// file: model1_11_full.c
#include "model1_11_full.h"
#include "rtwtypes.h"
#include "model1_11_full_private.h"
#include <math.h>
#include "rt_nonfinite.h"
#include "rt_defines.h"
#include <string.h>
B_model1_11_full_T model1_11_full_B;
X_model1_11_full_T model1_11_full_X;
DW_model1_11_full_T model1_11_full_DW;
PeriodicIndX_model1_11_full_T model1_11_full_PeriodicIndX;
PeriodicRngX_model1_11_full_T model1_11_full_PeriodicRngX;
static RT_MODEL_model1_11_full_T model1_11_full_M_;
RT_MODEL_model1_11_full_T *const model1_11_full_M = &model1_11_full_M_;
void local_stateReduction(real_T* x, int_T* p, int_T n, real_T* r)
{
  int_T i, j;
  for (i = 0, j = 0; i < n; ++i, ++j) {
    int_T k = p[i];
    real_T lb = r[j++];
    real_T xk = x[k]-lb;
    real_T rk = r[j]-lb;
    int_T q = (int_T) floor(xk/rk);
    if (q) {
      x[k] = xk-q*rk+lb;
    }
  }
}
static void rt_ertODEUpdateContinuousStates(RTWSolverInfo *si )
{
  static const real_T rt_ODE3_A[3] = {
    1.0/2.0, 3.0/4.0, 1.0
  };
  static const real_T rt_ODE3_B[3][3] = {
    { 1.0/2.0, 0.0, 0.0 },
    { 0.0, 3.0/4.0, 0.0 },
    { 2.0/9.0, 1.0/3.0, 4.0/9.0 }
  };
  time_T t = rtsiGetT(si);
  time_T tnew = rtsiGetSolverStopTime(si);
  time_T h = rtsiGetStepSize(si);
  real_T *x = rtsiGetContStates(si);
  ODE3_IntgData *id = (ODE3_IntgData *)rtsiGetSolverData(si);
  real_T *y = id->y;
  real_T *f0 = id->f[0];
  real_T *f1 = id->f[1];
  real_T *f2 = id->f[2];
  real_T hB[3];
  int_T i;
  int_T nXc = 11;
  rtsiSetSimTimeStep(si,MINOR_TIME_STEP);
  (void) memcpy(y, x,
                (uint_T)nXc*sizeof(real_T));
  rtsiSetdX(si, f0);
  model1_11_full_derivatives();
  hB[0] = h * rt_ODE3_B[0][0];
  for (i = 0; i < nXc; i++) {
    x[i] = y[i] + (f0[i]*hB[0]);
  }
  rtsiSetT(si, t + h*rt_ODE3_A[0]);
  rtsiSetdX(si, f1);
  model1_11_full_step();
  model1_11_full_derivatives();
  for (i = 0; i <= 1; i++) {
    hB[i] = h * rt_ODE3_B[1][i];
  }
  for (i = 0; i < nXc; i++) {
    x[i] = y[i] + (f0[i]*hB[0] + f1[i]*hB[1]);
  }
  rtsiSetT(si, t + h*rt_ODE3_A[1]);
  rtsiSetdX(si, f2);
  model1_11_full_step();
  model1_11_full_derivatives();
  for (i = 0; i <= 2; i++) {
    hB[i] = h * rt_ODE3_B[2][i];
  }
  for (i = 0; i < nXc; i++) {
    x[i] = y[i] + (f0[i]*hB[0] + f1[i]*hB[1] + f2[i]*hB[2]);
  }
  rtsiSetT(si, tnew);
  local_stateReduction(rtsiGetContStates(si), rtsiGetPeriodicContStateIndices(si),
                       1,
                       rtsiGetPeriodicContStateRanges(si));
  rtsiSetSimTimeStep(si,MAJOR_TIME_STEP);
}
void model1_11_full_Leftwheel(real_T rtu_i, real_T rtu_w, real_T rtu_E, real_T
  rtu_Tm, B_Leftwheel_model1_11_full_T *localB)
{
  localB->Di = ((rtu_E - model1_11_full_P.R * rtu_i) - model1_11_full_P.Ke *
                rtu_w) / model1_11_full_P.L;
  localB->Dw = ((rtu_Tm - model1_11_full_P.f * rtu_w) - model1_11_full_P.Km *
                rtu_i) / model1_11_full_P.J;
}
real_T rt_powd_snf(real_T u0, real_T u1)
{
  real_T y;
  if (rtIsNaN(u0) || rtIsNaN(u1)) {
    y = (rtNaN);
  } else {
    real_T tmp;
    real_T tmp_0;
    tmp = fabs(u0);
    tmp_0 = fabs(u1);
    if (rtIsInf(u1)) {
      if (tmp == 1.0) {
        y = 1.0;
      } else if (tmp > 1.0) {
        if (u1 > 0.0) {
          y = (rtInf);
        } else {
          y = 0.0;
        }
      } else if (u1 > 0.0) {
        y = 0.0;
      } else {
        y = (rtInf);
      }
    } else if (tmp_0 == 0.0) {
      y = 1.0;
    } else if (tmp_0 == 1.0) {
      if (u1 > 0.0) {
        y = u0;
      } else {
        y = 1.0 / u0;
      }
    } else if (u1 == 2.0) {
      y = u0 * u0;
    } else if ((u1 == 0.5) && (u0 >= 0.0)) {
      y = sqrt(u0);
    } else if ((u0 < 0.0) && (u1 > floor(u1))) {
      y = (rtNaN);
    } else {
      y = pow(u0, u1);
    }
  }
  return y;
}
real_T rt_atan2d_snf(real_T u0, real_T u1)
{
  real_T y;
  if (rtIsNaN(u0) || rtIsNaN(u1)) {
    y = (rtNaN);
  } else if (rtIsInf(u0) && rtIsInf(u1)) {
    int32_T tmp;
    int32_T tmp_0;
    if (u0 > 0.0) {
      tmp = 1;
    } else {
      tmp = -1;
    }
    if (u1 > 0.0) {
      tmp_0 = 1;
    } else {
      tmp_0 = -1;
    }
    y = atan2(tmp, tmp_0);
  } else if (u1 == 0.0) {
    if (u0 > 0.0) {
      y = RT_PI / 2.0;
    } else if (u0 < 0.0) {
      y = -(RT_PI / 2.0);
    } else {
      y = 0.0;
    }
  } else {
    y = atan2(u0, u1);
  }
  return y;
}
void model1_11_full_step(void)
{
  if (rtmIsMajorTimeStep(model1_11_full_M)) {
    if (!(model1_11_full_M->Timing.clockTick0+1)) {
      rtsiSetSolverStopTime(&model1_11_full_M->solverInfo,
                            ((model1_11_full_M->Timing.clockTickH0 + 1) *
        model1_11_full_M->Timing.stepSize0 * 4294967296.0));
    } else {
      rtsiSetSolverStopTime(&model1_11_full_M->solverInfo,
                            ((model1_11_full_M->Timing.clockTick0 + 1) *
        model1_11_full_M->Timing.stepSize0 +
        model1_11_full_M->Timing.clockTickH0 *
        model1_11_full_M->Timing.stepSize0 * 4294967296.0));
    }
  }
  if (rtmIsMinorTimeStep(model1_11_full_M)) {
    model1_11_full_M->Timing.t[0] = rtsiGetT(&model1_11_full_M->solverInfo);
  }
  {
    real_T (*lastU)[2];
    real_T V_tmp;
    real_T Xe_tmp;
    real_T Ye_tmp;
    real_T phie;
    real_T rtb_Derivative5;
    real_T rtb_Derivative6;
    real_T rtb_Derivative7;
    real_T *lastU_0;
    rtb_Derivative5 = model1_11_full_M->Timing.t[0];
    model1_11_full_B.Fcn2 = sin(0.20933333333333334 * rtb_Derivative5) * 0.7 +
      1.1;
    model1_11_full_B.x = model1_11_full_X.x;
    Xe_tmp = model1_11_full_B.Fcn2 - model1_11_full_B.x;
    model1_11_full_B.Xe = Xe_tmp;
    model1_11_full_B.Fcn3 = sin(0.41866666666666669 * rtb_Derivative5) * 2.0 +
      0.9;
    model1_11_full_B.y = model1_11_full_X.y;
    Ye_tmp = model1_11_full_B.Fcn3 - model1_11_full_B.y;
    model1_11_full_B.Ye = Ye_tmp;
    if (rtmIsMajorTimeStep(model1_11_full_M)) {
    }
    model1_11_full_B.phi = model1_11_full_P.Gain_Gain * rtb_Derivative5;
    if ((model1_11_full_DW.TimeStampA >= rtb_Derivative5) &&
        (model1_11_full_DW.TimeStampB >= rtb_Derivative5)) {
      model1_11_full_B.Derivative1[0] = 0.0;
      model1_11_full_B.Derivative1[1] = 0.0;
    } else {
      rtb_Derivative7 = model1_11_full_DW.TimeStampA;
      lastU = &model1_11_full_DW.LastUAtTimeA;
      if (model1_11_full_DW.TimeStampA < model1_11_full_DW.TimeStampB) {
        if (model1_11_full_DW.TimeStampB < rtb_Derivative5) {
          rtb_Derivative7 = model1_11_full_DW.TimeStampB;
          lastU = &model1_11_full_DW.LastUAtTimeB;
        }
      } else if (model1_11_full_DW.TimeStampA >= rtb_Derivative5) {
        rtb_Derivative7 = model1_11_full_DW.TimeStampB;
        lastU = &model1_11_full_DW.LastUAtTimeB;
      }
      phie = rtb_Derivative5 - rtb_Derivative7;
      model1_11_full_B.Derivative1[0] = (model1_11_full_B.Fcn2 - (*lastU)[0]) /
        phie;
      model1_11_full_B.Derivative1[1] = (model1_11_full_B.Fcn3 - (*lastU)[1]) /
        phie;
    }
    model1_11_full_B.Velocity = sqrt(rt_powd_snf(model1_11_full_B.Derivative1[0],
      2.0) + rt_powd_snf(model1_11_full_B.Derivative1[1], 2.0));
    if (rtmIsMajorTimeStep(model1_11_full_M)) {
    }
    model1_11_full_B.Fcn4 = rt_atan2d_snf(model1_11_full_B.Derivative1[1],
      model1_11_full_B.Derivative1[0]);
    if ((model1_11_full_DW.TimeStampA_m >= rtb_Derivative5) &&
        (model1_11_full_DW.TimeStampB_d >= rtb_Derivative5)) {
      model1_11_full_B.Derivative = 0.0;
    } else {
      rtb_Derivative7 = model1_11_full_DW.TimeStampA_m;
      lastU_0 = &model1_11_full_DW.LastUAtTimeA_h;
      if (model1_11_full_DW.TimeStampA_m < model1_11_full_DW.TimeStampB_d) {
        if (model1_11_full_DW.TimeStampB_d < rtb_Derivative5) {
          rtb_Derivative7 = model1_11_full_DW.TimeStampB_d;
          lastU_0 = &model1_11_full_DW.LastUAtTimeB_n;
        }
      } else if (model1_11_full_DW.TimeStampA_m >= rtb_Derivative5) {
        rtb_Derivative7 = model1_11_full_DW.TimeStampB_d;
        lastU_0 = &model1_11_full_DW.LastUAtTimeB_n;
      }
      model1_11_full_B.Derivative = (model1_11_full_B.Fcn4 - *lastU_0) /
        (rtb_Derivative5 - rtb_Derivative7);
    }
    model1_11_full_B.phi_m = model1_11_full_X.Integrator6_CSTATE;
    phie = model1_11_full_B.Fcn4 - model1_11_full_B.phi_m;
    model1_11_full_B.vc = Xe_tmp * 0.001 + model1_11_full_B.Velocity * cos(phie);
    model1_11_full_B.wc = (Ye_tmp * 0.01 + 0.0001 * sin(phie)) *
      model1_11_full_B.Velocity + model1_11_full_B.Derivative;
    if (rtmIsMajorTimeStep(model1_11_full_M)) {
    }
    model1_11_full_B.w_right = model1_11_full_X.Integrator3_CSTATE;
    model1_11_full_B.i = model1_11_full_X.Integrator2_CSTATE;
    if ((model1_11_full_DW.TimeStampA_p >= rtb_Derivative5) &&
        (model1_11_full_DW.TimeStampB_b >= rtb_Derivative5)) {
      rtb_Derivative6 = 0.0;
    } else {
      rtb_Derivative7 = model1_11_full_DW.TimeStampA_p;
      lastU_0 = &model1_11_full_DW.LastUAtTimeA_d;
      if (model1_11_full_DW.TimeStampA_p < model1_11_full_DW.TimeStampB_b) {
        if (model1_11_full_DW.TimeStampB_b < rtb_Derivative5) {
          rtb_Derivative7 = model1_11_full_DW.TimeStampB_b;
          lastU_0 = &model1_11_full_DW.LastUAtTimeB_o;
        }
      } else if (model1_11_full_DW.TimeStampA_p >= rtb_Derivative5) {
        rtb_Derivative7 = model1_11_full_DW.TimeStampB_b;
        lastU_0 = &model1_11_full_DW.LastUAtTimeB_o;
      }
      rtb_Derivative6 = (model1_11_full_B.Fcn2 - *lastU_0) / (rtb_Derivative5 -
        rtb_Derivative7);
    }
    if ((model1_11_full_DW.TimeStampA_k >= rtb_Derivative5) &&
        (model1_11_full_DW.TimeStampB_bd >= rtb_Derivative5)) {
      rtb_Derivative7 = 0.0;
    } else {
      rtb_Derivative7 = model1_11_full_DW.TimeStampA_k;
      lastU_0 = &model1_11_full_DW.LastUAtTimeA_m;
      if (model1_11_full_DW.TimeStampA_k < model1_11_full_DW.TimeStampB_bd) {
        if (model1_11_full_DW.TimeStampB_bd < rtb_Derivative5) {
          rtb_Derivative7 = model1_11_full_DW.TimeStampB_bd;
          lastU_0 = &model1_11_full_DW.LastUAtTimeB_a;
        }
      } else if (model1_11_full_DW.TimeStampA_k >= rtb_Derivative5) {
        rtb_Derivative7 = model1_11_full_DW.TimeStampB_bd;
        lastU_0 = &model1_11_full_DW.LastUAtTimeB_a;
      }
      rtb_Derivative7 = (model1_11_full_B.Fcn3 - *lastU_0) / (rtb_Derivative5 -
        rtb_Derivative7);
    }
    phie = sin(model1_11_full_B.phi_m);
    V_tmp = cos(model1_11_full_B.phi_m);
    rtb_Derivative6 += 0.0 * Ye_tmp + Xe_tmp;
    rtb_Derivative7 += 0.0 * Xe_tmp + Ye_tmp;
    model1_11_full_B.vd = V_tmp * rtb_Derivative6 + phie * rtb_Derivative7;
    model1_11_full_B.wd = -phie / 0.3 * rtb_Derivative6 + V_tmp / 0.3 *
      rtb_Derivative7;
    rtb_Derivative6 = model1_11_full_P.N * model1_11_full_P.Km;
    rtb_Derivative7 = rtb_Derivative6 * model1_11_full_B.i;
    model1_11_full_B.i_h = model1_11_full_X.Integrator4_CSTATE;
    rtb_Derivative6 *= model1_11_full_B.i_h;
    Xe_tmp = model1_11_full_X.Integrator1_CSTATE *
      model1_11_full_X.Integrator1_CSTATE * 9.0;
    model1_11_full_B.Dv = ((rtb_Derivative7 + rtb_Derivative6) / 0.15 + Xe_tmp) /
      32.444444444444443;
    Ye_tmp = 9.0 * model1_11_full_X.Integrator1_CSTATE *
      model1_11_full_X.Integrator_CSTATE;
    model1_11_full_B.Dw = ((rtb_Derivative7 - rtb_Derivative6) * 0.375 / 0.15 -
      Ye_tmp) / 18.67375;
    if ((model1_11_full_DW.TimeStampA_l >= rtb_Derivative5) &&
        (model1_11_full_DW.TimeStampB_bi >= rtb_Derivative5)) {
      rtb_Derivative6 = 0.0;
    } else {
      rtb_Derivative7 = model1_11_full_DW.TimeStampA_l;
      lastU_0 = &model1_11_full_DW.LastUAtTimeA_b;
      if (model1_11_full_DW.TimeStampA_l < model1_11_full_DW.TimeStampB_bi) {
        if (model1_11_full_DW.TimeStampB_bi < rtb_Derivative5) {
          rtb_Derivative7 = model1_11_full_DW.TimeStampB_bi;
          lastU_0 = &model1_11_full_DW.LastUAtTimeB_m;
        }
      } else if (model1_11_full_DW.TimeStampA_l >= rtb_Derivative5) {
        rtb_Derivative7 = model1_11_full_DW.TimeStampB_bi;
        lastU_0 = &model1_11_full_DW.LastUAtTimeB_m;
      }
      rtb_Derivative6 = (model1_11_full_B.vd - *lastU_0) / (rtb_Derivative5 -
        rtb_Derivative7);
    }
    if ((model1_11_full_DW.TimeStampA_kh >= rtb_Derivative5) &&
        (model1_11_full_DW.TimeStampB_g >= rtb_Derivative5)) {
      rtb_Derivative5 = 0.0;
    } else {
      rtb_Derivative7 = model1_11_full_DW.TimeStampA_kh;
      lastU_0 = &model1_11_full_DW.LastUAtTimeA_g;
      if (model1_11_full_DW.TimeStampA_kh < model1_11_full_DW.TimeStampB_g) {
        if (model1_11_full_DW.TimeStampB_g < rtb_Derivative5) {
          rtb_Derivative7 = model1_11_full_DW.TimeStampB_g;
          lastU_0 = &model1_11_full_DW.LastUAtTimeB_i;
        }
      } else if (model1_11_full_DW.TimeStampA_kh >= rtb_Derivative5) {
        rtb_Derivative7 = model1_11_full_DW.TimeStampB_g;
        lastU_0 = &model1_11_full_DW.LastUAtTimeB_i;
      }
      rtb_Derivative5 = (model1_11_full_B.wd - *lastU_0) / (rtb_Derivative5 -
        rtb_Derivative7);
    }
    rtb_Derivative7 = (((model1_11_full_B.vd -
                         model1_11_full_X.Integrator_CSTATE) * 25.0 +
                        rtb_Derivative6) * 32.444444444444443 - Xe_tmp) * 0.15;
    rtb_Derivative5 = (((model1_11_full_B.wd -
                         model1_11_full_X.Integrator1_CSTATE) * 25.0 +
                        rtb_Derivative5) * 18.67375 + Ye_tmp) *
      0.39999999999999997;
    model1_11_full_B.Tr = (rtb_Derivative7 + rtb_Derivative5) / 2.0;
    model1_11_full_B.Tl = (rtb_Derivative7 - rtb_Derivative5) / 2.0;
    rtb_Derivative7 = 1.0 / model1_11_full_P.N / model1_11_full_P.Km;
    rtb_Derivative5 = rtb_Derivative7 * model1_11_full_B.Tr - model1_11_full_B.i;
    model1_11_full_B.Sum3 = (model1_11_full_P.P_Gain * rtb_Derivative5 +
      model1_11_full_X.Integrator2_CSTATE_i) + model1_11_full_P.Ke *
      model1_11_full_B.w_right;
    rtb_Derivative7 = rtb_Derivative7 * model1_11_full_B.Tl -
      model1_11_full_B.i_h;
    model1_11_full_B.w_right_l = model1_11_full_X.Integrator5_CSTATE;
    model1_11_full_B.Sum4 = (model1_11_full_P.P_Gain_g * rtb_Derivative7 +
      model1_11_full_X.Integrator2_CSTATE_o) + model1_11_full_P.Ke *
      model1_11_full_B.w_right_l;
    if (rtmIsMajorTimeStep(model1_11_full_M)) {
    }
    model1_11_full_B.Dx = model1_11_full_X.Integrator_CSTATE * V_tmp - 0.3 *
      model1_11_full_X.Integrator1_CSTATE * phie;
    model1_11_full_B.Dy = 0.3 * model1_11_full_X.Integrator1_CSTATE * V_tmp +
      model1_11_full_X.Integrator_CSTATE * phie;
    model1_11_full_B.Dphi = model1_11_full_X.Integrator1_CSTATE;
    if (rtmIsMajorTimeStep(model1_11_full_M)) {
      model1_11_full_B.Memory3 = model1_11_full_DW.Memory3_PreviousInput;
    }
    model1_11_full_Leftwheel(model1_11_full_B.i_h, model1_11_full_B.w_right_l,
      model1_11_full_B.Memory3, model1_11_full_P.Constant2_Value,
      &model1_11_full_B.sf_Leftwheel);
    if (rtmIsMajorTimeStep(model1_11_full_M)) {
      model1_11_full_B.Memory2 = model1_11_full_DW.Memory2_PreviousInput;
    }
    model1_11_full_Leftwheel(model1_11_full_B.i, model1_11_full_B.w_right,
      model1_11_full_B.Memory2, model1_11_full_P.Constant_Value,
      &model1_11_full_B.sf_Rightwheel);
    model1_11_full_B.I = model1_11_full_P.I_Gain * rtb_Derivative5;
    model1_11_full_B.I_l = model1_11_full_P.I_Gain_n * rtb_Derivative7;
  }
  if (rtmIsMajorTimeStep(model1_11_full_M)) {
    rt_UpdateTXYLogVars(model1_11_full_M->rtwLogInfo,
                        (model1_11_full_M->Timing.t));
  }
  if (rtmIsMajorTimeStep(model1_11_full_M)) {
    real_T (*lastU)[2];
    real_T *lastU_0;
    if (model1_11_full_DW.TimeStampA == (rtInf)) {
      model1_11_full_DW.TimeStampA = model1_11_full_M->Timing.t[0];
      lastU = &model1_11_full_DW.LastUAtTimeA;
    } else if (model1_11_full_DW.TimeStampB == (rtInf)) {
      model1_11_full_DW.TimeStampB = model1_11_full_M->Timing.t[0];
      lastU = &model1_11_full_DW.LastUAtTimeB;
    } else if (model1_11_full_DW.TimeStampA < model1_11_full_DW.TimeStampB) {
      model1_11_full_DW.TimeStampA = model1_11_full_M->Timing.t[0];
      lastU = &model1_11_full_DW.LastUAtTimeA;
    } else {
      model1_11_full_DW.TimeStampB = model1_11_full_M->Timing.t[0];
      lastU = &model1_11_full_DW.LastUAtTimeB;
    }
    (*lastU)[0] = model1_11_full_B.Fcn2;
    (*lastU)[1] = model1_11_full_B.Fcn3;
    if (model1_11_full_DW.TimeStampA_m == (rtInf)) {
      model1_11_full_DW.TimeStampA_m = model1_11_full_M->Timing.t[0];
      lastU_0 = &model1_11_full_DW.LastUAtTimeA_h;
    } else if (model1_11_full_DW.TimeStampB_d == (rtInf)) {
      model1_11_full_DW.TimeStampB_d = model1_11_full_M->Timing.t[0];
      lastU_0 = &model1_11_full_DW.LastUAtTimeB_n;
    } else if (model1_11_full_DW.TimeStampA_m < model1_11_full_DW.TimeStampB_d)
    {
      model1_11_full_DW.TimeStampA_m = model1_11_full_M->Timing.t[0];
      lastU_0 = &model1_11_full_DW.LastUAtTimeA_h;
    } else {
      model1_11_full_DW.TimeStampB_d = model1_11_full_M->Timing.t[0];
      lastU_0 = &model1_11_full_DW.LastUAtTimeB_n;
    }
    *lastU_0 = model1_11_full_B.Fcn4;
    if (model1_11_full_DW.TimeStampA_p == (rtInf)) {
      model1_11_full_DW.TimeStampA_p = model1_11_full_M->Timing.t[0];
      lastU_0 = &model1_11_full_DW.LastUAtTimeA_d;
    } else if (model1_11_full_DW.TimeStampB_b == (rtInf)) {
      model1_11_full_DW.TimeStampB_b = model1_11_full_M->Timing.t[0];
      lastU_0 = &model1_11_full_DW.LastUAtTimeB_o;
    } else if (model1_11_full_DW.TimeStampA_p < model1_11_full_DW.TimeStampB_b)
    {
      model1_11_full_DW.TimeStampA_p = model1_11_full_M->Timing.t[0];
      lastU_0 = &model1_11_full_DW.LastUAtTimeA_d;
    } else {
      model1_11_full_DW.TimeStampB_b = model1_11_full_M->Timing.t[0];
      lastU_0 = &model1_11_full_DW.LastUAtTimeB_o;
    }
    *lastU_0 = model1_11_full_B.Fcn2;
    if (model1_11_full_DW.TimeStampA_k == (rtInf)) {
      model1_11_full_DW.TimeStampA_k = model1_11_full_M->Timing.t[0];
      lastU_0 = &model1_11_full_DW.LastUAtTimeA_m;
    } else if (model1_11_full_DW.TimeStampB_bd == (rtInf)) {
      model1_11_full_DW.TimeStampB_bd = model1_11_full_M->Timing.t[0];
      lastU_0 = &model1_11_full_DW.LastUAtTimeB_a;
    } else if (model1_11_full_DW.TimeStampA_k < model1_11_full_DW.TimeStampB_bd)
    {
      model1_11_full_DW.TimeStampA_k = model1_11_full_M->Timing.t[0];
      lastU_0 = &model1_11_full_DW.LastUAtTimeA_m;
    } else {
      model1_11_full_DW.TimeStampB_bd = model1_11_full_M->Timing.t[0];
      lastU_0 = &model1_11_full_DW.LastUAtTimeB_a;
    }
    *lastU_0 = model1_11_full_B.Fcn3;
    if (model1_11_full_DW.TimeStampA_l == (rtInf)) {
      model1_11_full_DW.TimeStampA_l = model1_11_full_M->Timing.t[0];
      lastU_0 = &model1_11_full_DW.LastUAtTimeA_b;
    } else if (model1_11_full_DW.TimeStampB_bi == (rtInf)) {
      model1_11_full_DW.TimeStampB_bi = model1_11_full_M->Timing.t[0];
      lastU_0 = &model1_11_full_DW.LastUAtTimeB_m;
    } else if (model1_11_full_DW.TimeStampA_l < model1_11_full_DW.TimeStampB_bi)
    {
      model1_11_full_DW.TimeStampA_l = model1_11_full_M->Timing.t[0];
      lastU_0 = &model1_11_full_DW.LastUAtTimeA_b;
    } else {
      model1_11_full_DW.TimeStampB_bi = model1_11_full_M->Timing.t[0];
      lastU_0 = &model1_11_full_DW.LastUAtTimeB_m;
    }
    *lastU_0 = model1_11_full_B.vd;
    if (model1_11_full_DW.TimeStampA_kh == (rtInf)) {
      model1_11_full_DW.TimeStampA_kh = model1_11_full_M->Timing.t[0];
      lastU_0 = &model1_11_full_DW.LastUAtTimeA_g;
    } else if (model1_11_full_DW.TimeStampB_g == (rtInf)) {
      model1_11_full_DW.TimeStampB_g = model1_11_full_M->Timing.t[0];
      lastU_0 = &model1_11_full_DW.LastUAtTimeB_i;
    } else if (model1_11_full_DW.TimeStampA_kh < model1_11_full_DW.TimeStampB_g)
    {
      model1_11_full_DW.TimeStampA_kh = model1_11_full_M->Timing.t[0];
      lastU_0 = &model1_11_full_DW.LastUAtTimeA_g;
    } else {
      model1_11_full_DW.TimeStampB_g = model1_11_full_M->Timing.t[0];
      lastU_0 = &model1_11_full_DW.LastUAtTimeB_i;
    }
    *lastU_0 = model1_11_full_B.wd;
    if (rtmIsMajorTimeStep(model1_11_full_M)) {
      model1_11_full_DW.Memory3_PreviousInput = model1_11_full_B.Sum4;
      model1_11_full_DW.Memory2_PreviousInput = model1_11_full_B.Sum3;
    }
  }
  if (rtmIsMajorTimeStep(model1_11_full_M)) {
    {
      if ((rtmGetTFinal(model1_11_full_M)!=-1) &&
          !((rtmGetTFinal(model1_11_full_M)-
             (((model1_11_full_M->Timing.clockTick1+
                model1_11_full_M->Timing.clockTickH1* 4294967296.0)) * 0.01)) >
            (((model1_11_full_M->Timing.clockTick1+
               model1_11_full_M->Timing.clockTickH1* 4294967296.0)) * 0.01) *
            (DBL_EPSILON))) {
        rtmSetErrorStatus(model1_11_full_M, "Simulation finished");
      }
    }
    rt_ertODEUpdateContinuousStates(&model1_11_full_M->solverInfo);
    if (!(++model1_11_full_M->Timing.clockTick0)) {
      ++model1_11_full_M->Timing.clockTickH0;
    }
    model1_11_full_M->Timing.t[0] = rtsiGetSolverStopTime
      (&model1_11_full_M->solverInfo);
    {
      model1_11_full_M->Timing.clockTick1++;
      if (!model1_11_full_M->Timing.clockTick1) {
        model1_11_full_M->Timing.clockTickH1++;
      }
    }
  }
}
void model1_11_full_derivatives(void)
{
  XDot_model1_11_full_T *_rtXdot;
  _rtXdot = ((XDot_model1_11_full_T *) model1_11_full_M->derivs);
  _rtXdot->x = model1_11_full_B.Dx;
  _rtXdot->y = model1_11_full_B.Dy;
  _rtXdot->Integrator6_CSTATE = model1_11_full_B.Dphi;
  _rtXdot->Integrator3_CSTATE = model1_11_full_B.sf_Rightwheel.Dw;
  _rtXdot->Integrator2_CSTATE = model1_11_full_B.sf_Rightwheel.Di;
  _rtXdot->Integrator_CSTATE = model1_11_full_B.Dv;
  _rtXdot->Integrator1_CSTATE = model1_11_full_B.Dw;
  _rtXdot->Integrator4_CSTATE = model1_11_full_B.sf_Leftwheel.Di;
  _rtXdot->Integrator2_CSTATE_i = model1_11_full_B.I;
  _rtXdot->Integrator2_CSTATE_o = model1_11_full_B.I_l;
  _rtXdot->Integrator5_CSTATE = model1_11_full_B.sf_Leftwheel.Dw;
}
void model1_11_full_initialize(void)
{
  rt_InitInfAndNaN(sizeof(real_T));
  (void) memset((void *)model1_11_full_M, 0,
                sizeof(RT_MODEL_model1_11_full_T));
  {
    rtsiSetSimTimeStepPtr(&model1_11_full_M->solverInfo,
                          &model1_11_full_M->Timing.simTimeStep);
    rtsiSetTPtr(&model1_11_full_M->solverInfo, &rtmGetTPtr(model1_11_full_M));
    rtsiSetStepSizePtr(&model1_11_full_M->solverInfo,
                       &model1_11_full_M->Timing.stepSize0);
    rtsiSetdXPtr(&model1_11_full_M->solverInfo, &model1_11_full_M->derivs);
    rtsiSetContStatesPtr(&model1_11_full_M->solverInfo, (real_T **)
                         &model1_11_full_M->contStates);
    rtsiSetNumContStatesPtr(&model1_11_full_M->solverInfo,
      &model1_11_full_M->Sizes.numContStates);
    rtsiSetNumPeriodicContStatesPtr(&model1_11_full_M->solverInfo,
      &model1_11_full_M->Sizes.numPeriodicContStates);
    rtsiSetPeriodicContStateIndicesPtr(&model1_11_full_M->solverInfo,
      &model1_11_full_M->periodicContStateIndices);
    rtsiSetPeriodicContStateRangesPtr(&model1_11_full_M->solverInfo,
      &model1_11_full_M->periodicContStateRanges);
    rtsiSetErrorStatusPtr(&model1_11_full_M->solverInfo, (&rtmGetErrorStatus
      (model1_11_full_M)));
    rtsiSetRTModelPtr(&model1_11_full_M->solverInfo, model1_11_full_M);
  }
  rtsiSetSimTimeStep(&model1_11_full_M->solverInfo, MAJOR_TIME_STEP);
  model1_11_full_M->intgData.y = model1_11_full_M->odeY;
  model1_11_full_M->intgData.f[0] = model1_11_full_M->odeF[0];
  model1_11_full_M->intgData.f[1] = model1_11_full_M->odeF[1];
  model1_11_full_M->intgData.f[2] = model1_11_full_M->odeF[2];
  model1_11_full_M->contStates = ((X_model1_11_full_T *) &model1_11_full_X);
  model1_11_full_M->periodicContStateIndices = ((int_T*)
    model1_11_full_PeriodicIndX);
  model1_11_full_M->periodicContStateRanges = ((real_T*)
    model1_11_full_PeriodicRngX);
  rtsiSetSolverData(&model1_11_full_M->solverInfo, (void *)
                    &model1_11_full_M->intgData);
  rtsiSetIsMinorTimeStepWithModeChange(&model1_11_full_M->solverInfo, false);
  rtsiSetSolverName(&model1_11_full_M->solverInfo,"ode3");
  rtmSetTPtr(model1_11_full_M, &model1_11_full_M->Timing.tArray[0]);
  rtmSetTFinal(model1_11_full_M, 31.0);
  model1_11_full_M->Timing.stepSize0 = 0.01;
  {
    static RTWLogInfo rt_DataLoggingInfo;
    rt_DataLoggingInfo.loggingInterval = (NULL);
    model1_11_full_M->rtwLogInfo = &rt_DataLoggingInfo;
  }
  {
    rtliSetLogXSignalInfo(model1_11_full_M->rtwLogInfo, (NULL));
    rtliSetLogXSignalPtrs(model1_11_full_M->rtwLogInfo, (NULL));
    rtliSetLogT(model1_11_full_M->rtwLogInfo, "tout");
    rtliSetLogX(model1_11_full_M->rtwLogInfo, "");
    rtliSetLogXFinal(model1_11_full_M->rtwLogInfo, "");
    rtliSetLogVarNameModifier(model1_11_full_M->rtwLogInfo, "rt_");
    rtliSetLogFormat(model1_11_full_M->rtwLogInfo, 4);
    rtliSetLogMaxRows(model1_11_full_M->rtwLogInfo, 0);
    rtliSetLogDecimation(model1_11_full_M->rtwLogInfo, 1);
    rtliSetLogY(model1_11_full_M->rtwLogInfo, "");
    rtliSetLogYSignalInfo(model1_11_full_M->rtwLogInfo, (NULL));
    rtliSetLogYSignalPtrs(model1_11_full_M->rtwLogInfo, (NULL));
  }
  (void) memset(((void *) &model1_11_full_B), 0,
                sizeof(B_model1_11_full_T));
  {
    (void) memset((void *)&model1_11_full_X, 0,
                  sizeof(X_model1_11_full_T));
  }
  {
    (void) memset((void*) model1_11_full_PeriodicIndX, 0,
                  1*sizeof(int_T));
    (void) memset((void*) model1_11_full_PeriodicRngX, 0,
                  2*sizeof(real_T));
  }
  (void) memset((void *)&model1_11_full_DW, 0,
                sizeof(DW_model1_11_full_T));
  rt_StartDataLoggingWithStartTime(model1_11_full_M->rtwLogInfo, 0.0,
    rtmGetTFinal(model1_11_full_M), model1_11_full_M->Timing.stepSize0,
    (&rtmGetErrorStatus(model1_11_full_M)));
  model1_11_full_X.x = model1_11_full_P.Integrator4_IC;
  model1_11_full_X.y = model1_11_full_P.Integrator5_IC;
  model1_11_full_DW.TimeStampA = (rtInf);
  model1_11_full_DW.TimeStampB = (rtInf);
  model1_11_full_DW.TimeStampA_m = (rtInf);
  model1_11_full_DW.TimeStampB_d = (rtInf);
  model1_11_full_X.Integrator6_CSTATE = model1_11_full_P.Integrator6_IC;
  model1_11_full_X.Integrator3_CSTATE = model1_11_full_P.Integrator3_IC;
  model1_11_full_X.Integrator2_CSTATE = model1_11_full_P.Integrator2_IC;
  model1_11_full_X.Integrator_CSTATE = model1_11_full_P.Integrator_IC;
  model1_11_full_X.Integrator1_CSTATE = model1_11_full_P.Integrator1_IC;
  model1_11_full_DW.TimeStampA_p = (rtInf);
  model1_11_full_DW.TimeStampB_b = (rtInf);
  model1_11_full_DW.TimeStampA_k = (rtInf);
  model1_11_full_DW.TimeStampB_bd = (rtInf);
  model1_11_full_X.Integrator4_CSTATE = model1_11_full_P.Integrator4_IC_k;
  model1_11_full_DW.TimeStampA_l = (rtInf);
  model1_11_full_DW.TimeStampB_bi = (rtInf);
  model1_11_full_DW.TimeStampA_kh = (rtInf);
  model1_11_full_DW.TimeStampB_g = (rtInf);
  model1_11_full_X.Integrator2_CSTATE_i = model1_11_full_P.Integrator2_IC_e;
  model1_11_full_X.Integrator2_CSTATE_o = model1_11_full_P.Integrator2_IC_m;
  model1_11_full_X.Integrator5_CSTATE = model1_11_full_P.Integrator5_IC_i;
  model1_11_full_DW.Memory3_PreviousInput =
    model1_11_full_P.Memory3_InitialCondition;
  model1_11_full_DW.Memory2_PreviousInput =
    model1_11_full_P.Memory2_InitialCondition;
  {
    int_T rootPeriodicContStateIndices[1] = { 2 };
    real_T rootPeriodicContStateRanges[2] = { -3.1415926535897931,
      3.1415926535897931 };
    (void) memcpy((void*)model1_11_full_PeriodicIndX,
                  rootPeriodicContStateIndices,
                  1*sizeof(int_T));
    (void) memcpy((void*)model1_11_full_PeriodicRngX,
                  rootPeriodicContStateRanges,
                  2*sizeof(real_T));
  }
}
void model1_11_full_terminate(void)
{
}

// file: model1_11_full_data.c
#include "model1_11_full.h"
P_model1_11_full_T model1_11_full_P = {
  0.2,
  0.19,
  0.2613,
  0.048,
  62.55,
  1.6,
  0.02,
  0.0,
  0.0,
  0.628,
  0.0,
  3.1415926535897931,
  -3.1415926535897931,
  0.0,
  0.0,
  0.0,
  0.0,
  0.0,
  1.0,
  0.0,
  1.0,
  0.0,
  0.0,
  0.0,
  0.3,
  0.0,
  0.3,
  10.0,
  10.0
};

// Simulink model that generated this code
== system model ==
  Sum#1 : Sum  Inputs=+-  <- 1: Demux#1, 2: Integrator4
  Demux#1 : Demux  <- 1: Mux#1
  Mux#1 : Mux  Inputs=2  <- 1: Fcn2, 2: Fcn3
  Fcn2 : Fcn  Expr=1.1+0.7*sin(2*3.14/30*u(1))  <- 1: Clock#1
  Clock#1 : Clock
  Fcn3 : Fcn  Expr=0.9+2*sin(4*3.14/30*u(1))  <- 1: Clock#1
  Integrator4 : Integrator  <- 1: MATLABFunction#1
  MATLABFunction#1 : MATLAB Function  <- 1: Integrator, 2: Integrator1, 3: Integrator6
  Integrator : Integrator  <- 1: MATLABFunction#2
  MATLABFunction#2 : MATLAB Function  <- 1: Gain#1, 2: Gain#2, 3: Integrator, 4: Integrator1
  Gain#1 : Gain  Gain=N*Km  <- 1: Integrator2
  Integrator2 : Integrator  <- 1: Rightwheel
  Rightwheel : MATLAB Function  <- 1: Integrator2, 2: Integrator3, 3: Memory2, 4: Constant
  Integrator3 : Integrator  <- 1: Rightwheel/2
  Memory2 : Memory  <- 1: Sum3
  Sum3 : Sum  Inputs=++  <- 1: Gain#3, 2: Sum#2
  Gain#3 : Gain  Gain=Ke  <- 1: Integrator3
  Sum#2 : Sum  Inputs=+++  <- 1: Gain#4, 2: Integrator#1
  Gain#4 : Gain  <- 1: Sum#3
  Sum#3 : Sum  Inputs=-+  <- 1: Integrator2, 2: Gain#5
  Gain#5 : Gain  Gain=1/N/Km  <- 1: MATLABFunction#3
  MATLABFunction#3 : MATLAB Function  <- 1: Integrator, 2: Integrator1, 3: MATLABFunction#4, 4: MATLABFunction#4/2, 5: MATLABFunction#2, 6: MATLABFunction#2/2, 7: Derivative#1, 8: Derivative5
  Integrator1 : Integrator  <- 1: MATLABFunction#2/2
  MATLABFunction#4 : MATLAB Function  <- 1: Derivative6, 2: Derivative7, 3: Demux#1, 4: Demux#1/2, 5: Integrator4, 6: Integrator5, 7: Integrator6
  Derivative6 : Derivative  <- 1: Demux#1
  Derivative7 : Derivative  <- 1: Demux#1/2
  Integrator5 : Integrator  <- 1: MATLABFunction#1/2
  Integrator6 : Integrator  <- 1: MATLABFunction#1/3
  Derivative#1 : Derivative  <- 1: MATLABFunction#4
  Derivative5 : Derivative  <- 1: MATLABFunction#4/2
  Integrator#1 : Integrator  <- 1: Gain#6
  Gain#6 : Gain  Gain=10  <- 1: Sum#3
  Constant : Constant  Value=0.3
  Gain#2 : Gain  Gain=N*Km  <- 1: Integrator#2
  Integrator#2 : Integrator  <- 1: Leftwheel
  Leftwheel : MATLAB Function  <- 1: Integrator#2, 2: Integrator#3, 3: Memory3, 4: Constant2
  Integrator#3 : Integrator  <- 1: Leftwheel/2
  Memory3 : Memory  <- 1: Sum4
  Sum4 : Sum  Inputs=++  <- 1: Sum#4, 2: Gain#7
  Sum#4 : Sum  Inputs=+++  <- 1: Gain#8, 2: Integrator#4
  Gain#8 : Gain  <- 1: Sum#5
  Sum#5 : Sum  Inputs=+-  <- 1: Gain#9, 2: Integrator#2
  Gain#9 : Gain  Gain=1/N/Km  <- 1: MATLABFunction#3/2
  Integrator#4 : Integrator  <- 1: Gain#10
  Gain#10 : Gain  Gain=10  <- 1: Sum#5
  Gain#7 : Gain  Gain=Ke  <- 1: Integrator#3
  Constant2 : Constant  Value=0.3
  MATLABFunction#5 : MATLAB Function  <- 1: Integrator4, 2: Integrator5, 3: Integrator6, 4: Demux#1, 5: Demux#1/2, 6: Fcn4, 7: Velocity, 8: Derivative
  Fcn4 : Fcn  Expr=atan2(u(2),u(1))  <- 1: Derivative1
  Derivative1 : Derivative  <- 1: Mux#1
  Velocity : Fcn  Expr=sqrt(u(1)^2+u(2)^2)  <- 1: Derivative1
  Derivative : Derivative  <- 1: Fcn4
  Sum#6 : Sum  Inputs=+-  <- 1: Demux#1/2, 2: Integrator5
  Gain : Gain  Gain=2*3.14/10  <- 1: Clock#1
== matlab function MATLABFunction#5 ==
function [vc,wc] = fcn(x,y,phi,xr,yr,phir,vr,wr)
Kx = 0.001; Ky = .01; Kphi = 0.0001;

xe = xr - x;
ye = yr - y;
phie = phir - phi;

vc = vr*cos(phie) + Kx*xe;
wc = wr + vr*(Ky*ye + Kphi*sin(phie));

== matlab function MATLABFunction#2 ==
function [Dv,Dw] = fcn(Tr,Tl,v,w)
mc = 30; Ic = 15.625; R = 0.15; L = 0.375;
d = 0.3; Iw = 0.005; Im = 0.0025; mw = 1;

I = Ic + mc*d^2 + 2*mw*L^2 + 2*Im;
m = mc + 2*mw;

Dv = ((Tr+Tl)/R  + mc*d*w^2)/(m + 2*Iw/R^2);
Dw = ((Tr-Tl)*L/R- mc*d*w*v)/(I + 2*(L/R)^2*Iw);
end

== matlab function Rightwheel ==
function [Di,Dw] = fcn(i,w,E,Tm,R, Ke, Km, J, f,L)
Di = (E-R*i-Ke*w)/L;
Dw = (Tm - f*w -Km*i)/J;
end

== matlab function Leftwheel ==
function [Di,Dw] = fcn(i,w,E,Tm,R, Ke, Km, J, f,L)
Di = (E-R*i-Ke*w)/L;
Dw = (Tm - f*w -Km*i)/J;
end

== matlab function MATLABFunction#1 ==
function [Dx,Dy,Dphi] = fcn(v,w,phi)

d = 0.3;
Dx = v*cos(phi) - d*w*sin(phi);
Dy = v*sin(phi) + d*w*cos(phi);
Dphi = w;
%{
Dx = v*cos(phi);
Dy = v*sin(phi);
Dphi = w;
%}
end

== matlab function MATLABFunction#3 ==
function [Tr,Tl] = fcn(v,w,vr,wr,dv,dw,dvr,dwr)
mc = 30; Ic = 15.625; R = 0.15; L = 0.375;
d = 0.3; Iw = 0.005; Im = 0.0025; mw = 1;
I = Ic + mc*d^2 + 2*mw*L^2 + 2*Im;
m = mc + 2*mw;

Kv = 25; Kw = 25;

Ev = vr - v;
Ew = wr - w;

a = R  * ((dvr + Kv*Ev)*(m + 2*Iw/R^2)     - mc*d*w^2);
b = R/L* ((dwr + Kw*Ew)*(I + 2*L^2*Iw/R^2) + mc*d*w*v);

Tr = (a + b)/2;
Tl = (a - b)/2;
end

== matlab function MATLABFunction#4 ==
function [vd,wd] = fcn(dxr,dyr,xr,yr,x,y,phi)
d = 0.3; Kx = 1; Ky = 1;

Ex = xr - x;
Ey = yr - y;

V = [cos(phi), sin(phi);...
    -sin(phi)/d, cos(phi)/d] *([dxr;dyr] + diag([Kx,Ky])*[Ex;Ey]);
vd = V(1);
wd = V(2);

end
